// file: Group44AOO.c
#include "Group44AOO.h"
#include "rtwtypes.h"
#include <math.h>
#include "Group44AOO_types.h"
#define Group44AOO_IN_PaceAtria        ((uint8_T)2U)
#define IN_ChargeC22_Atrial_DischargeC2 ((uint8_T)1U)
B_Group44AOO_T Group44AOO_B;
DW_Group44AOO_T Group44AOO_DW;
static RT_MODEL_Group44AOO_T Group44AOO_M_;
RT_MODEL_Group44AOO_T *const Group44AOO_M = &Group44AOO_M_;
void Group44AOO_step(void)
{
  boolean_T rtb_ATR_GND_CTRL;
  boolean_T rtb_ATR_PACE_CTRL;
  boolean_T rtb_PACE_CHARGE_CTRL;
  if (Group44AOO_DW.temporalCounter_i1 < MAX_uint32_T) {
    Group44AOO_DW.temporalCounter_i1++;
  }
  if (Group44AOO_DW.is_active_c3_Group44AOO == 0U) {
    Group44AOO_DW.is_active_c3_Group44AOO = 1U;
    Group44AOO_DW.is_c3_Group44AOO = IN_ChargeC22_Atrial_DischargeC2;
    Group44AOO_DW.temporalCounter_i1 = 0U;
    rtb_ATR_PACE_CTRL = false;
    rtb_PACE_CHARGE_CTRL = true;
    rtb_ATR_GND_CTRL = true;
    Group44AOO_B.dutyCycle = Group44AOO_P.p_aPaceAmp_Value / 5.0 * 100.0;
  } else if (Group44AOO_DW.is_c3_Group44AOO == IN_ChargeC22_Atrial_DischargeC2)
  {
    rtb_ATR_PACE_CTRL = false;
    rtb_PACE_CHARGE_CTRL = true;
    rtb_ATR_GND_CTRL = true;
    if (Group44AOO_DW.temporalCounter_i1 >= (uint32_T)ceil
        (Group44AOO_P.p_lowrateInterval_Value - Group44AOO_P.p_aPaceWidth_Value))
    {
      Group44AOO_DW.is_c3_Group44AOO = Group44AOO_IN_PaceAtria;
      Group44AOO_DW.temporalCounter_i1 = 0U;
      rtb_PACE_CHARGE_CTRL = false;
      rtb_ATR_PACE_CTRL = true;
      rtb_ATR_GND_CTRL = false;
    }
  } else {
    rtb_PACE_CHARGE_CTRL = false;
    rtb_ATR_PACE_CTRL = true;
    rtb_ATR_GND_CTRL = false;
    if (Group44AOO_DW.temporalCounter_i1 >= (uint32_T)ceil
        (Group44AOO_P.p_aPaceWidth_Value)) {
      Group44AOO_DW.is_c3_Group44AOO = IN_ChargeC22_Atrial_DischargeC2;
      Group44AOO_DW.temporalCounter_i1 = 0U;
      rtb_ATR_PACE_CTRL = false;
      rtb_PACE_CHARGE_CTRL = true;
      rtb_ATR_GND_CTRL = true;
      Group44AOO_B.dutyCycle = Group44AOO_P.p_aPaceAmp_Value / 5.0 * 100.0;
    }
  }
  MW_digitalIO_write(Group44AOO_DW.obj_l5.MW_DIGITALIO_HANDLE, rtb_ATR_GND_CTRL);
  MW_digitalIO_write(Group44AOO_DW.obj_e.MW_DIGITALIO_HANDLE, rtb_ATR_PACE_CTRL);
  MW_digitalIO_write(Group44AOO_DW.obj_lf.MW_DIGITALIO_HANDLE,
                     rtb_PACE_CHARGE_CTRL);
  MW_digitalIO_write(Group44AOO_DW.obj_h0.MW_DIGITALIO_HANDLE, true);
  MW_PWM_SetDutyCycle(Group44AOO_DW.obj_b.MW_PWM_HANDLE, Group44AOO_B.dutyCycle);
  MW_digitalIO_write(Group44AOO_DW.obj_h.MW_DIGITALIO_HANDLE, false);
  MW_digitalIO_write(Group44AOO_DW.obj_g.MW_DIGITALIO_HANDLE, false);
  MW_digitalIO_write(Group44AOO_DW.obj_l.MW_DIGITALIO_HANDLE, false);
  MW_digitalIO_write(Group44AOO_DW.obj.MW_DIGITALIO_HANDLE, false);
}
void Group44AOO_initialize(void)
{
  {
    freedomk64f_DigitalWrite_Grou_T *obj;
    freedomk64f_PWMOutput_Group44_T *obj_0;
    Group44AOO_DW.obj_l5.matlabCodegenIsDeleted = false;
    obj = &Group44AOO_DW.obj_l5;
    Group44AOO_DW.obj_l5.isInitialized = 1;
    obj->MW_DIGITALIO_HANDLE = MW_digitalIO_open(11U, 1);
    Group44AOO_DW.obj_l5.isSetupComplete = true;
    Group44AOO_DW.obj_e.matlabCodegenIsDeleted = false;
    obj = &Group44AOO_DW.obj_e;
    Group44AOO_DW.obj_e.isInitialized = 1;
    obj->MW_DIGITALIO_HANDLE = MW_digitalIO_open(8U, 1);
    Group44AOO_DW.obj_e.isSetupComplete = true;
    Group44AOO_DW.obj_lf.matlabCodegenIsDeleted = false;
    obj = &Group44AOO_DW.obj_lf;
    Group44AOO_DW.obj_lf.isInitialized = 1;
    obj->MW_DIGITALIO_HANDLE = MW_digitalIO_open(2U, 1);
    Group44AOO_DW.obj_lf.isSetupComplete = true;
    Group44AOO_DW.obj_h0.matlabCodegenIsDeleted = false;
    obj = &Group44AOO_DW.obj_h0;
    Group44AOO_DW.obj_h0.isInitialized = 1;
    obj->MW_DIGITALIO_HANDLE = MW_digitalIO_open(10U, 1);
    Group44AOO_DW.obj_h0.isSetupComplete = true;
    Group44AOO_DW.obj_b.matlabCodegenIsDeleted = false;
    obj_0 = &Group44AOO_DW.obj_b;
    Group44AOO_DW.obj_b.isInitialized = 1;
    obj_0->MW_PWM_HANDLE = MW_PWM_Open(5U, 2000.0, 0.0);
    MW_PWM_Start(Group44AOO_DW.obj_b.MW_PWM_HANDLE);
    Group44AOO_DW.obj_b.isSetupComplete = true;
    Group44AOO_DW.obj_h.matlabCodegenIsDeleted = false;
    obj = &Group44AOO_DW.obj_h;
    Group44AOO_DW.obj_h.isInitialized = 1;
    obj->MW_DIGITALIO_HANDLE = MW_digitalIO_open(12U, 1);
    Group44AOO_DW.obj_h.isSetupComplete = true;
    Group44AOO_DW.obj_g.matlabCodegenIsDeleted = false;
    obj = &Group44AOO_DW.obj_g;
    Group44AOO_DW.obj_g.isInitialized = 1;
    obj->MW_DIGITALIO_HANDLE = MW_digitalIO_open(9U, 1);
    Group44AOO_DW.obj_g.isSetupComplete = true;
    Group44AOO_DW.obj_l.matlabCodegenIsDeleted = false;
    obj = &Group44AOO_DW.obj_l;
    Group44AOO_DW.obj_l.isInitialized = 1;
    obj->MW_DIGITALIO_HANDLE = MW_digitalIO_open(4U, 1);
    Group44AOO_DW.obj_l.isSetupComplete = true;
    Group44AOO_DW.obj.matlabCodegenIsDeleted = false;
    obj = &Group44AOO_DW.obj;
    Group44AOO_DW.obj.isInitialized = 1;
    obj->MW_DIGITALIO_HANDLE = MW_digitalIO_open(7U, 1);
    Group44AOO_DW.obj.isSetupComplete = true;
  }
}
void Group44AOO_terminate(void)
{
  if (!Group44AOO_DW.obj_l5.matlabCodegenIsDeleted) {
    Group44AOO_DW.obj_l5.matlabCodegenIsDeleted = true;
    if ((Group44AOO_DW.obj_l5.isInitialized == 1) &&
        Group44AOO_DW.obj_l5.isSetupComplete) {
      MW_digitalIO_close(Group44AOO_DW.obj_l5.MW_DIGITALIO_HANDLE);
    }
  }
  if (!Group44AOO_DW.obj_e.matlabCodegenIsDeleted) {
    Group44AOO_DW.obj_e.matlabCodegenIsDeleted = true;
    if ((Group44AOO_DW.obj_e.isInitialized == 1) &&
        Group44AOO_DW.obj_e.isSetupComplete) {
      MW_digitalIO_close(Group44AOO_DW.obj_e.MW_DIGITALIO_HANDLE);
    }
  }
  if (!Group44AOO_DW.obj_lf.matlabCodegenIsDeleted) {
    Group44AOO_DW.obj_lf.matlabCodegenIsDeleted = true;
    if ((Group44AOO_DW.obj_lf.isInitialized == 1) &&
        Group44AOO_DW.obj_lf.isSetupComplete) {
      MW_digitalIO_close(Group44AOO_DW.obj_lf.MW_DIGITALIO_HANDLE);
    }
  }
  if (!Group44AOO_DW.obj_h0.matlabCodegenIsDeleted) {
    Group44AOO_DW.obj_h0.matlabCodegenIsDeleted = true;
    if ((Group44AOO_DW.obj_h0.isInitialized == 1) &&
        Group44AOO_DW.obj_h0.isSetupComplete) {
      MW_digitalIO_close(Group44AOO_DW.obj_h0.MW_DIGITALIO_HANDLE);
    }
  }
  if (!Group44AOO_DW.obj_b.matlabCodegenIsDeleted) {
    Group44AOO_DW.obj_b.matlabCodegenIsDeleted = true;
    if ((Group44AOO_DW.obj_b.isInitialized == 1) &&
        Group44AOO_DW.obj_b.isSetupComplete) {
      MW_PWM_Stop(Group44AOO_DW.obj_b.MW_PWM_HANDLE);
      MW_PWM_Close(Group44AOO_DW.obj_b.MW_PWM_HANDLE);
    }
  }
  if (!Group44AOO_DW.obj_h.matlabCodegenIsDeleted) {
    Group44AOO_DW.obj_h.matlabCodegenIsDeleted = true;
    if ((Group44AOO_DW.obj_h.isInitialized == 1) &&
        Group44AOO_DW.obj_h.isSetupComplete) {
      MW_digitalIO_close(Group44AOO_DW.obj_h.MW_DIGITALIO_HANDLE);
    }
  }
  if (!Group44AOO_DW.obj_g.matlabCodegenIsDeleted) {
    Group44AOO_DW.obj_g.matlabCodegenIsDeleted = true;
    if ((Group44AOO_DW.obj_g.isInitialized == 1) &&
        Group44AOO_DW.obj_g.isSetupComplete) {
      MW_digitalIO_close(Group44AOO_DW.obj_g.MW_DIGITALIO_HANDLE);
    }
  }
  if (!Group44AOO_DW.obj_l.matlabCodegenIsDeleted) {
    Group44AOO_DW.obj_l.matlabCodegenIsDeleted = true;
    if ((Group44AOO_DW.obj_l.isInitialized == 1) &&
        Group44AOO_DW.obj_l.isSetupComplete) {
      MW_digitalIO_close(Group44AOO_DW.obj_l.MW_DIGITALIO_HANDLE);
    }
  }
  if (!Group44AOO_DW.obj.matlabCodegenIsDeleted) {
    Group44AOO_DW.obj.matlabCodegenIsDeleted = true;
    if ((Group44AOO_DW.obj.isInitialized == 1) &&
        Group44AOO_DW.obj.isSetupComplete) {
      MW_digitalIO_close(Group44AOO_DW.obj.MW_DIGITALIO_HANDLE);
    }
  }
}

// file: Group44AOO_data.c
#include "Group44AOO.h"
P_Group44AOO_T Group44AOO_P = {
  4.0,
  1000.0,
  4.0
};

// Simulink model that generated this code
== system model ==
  ATR_GND_CTRL : frdmk64flib/Digital Write  <- 1: Stateflowchart#1
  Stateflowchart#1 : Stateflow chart  <- 1: p_aPaceWidth, 2: p_lowrateInterval, 3: p_aPaceAmp
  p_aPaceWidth : Constant  Value=4
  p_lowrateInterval : Constant  Value=1000
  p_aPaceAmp : Constant  Value=4
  ATR_PACE_CTRL : frdmk64flib/Digital Write  <- 1: Stateflowchart#1/2
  PACE_CHARGE_CTRL : frdmk64flib/Digital Write  <- 1: Stateflowchart#1/3
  DigitalWrite#1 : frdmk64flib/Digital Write  <- 1: Stateflowchart#1/4
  PWMOutput#1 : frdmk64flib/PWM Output  <- 1: Stateflowchart#1/9
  DigitalWrite#2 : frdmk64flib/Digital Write  <- 1: Stateflowchart#1/5
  DigitalWrite#3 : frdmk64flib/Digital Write  <- 1: Stateflowchart#1/6
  DigitalWrite#4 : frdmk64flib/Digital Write  <- 1: Stateflowchart#1/7
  DigitalWrite#5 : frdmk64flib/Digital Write  <- 1: Stateflowchart#1/8
== stateflow chart Stateflowchart#1 ==
  state ChargeC22_Atrial_DischargeC21
    entry:
    ATR_PACE_CTRL = false;
    VENT_PACE_CTRL = false;
    PACE_CHARGE_CTRL = true;
    PACE_GND_CTRL = true;
    Z_ATR_CTRL = false;
    Z_VENT_CTRL = false;
    ATR_GND_CTRL = true;
    VENT_GND_CTRL = false;
    dutyCycle=p_aPaceAmp/5.0*100
  state PaceAtria
    entry:
    PACE_CHARGE_CTRL = false;
    PACE_GND_CTRL = true;
    ATR_PACE_CTRL = true;
    ATR_GND_CTRL = false;
    Z_ATR_CTRL = false;
    Z_VENT_CTRL = false;
    VENT_GND_CTRL = false;
    VENT_PACE_CTRL = false;
    %natPaceDetected=false;
  (default) -> ChargeC22_Atrial_DischargeC21
  ChargeC22_Atrial_DischargeC21 -> PaceAtria : after(p_lowrateInterval-p_aPaceWidth,msec)
  PaceAtria -> ChargeC22_Atrial_DischargeC21 : after(p_aPaceWidth,msec)
  data: p_aPaceWidth input; p_lowrateInterval input; ATR_GND_CTRL output; ATR_PACE_CTRL output; PACE_CHARGE_CTRL output; PACE_GND_CTRL output; VENT_GND_CTRL output; VENT_PACE_CTRL output; Z_ATR_CTRL output; Z_VENT_CTRL output; dutyCycle output; p_aPaceAmp input
